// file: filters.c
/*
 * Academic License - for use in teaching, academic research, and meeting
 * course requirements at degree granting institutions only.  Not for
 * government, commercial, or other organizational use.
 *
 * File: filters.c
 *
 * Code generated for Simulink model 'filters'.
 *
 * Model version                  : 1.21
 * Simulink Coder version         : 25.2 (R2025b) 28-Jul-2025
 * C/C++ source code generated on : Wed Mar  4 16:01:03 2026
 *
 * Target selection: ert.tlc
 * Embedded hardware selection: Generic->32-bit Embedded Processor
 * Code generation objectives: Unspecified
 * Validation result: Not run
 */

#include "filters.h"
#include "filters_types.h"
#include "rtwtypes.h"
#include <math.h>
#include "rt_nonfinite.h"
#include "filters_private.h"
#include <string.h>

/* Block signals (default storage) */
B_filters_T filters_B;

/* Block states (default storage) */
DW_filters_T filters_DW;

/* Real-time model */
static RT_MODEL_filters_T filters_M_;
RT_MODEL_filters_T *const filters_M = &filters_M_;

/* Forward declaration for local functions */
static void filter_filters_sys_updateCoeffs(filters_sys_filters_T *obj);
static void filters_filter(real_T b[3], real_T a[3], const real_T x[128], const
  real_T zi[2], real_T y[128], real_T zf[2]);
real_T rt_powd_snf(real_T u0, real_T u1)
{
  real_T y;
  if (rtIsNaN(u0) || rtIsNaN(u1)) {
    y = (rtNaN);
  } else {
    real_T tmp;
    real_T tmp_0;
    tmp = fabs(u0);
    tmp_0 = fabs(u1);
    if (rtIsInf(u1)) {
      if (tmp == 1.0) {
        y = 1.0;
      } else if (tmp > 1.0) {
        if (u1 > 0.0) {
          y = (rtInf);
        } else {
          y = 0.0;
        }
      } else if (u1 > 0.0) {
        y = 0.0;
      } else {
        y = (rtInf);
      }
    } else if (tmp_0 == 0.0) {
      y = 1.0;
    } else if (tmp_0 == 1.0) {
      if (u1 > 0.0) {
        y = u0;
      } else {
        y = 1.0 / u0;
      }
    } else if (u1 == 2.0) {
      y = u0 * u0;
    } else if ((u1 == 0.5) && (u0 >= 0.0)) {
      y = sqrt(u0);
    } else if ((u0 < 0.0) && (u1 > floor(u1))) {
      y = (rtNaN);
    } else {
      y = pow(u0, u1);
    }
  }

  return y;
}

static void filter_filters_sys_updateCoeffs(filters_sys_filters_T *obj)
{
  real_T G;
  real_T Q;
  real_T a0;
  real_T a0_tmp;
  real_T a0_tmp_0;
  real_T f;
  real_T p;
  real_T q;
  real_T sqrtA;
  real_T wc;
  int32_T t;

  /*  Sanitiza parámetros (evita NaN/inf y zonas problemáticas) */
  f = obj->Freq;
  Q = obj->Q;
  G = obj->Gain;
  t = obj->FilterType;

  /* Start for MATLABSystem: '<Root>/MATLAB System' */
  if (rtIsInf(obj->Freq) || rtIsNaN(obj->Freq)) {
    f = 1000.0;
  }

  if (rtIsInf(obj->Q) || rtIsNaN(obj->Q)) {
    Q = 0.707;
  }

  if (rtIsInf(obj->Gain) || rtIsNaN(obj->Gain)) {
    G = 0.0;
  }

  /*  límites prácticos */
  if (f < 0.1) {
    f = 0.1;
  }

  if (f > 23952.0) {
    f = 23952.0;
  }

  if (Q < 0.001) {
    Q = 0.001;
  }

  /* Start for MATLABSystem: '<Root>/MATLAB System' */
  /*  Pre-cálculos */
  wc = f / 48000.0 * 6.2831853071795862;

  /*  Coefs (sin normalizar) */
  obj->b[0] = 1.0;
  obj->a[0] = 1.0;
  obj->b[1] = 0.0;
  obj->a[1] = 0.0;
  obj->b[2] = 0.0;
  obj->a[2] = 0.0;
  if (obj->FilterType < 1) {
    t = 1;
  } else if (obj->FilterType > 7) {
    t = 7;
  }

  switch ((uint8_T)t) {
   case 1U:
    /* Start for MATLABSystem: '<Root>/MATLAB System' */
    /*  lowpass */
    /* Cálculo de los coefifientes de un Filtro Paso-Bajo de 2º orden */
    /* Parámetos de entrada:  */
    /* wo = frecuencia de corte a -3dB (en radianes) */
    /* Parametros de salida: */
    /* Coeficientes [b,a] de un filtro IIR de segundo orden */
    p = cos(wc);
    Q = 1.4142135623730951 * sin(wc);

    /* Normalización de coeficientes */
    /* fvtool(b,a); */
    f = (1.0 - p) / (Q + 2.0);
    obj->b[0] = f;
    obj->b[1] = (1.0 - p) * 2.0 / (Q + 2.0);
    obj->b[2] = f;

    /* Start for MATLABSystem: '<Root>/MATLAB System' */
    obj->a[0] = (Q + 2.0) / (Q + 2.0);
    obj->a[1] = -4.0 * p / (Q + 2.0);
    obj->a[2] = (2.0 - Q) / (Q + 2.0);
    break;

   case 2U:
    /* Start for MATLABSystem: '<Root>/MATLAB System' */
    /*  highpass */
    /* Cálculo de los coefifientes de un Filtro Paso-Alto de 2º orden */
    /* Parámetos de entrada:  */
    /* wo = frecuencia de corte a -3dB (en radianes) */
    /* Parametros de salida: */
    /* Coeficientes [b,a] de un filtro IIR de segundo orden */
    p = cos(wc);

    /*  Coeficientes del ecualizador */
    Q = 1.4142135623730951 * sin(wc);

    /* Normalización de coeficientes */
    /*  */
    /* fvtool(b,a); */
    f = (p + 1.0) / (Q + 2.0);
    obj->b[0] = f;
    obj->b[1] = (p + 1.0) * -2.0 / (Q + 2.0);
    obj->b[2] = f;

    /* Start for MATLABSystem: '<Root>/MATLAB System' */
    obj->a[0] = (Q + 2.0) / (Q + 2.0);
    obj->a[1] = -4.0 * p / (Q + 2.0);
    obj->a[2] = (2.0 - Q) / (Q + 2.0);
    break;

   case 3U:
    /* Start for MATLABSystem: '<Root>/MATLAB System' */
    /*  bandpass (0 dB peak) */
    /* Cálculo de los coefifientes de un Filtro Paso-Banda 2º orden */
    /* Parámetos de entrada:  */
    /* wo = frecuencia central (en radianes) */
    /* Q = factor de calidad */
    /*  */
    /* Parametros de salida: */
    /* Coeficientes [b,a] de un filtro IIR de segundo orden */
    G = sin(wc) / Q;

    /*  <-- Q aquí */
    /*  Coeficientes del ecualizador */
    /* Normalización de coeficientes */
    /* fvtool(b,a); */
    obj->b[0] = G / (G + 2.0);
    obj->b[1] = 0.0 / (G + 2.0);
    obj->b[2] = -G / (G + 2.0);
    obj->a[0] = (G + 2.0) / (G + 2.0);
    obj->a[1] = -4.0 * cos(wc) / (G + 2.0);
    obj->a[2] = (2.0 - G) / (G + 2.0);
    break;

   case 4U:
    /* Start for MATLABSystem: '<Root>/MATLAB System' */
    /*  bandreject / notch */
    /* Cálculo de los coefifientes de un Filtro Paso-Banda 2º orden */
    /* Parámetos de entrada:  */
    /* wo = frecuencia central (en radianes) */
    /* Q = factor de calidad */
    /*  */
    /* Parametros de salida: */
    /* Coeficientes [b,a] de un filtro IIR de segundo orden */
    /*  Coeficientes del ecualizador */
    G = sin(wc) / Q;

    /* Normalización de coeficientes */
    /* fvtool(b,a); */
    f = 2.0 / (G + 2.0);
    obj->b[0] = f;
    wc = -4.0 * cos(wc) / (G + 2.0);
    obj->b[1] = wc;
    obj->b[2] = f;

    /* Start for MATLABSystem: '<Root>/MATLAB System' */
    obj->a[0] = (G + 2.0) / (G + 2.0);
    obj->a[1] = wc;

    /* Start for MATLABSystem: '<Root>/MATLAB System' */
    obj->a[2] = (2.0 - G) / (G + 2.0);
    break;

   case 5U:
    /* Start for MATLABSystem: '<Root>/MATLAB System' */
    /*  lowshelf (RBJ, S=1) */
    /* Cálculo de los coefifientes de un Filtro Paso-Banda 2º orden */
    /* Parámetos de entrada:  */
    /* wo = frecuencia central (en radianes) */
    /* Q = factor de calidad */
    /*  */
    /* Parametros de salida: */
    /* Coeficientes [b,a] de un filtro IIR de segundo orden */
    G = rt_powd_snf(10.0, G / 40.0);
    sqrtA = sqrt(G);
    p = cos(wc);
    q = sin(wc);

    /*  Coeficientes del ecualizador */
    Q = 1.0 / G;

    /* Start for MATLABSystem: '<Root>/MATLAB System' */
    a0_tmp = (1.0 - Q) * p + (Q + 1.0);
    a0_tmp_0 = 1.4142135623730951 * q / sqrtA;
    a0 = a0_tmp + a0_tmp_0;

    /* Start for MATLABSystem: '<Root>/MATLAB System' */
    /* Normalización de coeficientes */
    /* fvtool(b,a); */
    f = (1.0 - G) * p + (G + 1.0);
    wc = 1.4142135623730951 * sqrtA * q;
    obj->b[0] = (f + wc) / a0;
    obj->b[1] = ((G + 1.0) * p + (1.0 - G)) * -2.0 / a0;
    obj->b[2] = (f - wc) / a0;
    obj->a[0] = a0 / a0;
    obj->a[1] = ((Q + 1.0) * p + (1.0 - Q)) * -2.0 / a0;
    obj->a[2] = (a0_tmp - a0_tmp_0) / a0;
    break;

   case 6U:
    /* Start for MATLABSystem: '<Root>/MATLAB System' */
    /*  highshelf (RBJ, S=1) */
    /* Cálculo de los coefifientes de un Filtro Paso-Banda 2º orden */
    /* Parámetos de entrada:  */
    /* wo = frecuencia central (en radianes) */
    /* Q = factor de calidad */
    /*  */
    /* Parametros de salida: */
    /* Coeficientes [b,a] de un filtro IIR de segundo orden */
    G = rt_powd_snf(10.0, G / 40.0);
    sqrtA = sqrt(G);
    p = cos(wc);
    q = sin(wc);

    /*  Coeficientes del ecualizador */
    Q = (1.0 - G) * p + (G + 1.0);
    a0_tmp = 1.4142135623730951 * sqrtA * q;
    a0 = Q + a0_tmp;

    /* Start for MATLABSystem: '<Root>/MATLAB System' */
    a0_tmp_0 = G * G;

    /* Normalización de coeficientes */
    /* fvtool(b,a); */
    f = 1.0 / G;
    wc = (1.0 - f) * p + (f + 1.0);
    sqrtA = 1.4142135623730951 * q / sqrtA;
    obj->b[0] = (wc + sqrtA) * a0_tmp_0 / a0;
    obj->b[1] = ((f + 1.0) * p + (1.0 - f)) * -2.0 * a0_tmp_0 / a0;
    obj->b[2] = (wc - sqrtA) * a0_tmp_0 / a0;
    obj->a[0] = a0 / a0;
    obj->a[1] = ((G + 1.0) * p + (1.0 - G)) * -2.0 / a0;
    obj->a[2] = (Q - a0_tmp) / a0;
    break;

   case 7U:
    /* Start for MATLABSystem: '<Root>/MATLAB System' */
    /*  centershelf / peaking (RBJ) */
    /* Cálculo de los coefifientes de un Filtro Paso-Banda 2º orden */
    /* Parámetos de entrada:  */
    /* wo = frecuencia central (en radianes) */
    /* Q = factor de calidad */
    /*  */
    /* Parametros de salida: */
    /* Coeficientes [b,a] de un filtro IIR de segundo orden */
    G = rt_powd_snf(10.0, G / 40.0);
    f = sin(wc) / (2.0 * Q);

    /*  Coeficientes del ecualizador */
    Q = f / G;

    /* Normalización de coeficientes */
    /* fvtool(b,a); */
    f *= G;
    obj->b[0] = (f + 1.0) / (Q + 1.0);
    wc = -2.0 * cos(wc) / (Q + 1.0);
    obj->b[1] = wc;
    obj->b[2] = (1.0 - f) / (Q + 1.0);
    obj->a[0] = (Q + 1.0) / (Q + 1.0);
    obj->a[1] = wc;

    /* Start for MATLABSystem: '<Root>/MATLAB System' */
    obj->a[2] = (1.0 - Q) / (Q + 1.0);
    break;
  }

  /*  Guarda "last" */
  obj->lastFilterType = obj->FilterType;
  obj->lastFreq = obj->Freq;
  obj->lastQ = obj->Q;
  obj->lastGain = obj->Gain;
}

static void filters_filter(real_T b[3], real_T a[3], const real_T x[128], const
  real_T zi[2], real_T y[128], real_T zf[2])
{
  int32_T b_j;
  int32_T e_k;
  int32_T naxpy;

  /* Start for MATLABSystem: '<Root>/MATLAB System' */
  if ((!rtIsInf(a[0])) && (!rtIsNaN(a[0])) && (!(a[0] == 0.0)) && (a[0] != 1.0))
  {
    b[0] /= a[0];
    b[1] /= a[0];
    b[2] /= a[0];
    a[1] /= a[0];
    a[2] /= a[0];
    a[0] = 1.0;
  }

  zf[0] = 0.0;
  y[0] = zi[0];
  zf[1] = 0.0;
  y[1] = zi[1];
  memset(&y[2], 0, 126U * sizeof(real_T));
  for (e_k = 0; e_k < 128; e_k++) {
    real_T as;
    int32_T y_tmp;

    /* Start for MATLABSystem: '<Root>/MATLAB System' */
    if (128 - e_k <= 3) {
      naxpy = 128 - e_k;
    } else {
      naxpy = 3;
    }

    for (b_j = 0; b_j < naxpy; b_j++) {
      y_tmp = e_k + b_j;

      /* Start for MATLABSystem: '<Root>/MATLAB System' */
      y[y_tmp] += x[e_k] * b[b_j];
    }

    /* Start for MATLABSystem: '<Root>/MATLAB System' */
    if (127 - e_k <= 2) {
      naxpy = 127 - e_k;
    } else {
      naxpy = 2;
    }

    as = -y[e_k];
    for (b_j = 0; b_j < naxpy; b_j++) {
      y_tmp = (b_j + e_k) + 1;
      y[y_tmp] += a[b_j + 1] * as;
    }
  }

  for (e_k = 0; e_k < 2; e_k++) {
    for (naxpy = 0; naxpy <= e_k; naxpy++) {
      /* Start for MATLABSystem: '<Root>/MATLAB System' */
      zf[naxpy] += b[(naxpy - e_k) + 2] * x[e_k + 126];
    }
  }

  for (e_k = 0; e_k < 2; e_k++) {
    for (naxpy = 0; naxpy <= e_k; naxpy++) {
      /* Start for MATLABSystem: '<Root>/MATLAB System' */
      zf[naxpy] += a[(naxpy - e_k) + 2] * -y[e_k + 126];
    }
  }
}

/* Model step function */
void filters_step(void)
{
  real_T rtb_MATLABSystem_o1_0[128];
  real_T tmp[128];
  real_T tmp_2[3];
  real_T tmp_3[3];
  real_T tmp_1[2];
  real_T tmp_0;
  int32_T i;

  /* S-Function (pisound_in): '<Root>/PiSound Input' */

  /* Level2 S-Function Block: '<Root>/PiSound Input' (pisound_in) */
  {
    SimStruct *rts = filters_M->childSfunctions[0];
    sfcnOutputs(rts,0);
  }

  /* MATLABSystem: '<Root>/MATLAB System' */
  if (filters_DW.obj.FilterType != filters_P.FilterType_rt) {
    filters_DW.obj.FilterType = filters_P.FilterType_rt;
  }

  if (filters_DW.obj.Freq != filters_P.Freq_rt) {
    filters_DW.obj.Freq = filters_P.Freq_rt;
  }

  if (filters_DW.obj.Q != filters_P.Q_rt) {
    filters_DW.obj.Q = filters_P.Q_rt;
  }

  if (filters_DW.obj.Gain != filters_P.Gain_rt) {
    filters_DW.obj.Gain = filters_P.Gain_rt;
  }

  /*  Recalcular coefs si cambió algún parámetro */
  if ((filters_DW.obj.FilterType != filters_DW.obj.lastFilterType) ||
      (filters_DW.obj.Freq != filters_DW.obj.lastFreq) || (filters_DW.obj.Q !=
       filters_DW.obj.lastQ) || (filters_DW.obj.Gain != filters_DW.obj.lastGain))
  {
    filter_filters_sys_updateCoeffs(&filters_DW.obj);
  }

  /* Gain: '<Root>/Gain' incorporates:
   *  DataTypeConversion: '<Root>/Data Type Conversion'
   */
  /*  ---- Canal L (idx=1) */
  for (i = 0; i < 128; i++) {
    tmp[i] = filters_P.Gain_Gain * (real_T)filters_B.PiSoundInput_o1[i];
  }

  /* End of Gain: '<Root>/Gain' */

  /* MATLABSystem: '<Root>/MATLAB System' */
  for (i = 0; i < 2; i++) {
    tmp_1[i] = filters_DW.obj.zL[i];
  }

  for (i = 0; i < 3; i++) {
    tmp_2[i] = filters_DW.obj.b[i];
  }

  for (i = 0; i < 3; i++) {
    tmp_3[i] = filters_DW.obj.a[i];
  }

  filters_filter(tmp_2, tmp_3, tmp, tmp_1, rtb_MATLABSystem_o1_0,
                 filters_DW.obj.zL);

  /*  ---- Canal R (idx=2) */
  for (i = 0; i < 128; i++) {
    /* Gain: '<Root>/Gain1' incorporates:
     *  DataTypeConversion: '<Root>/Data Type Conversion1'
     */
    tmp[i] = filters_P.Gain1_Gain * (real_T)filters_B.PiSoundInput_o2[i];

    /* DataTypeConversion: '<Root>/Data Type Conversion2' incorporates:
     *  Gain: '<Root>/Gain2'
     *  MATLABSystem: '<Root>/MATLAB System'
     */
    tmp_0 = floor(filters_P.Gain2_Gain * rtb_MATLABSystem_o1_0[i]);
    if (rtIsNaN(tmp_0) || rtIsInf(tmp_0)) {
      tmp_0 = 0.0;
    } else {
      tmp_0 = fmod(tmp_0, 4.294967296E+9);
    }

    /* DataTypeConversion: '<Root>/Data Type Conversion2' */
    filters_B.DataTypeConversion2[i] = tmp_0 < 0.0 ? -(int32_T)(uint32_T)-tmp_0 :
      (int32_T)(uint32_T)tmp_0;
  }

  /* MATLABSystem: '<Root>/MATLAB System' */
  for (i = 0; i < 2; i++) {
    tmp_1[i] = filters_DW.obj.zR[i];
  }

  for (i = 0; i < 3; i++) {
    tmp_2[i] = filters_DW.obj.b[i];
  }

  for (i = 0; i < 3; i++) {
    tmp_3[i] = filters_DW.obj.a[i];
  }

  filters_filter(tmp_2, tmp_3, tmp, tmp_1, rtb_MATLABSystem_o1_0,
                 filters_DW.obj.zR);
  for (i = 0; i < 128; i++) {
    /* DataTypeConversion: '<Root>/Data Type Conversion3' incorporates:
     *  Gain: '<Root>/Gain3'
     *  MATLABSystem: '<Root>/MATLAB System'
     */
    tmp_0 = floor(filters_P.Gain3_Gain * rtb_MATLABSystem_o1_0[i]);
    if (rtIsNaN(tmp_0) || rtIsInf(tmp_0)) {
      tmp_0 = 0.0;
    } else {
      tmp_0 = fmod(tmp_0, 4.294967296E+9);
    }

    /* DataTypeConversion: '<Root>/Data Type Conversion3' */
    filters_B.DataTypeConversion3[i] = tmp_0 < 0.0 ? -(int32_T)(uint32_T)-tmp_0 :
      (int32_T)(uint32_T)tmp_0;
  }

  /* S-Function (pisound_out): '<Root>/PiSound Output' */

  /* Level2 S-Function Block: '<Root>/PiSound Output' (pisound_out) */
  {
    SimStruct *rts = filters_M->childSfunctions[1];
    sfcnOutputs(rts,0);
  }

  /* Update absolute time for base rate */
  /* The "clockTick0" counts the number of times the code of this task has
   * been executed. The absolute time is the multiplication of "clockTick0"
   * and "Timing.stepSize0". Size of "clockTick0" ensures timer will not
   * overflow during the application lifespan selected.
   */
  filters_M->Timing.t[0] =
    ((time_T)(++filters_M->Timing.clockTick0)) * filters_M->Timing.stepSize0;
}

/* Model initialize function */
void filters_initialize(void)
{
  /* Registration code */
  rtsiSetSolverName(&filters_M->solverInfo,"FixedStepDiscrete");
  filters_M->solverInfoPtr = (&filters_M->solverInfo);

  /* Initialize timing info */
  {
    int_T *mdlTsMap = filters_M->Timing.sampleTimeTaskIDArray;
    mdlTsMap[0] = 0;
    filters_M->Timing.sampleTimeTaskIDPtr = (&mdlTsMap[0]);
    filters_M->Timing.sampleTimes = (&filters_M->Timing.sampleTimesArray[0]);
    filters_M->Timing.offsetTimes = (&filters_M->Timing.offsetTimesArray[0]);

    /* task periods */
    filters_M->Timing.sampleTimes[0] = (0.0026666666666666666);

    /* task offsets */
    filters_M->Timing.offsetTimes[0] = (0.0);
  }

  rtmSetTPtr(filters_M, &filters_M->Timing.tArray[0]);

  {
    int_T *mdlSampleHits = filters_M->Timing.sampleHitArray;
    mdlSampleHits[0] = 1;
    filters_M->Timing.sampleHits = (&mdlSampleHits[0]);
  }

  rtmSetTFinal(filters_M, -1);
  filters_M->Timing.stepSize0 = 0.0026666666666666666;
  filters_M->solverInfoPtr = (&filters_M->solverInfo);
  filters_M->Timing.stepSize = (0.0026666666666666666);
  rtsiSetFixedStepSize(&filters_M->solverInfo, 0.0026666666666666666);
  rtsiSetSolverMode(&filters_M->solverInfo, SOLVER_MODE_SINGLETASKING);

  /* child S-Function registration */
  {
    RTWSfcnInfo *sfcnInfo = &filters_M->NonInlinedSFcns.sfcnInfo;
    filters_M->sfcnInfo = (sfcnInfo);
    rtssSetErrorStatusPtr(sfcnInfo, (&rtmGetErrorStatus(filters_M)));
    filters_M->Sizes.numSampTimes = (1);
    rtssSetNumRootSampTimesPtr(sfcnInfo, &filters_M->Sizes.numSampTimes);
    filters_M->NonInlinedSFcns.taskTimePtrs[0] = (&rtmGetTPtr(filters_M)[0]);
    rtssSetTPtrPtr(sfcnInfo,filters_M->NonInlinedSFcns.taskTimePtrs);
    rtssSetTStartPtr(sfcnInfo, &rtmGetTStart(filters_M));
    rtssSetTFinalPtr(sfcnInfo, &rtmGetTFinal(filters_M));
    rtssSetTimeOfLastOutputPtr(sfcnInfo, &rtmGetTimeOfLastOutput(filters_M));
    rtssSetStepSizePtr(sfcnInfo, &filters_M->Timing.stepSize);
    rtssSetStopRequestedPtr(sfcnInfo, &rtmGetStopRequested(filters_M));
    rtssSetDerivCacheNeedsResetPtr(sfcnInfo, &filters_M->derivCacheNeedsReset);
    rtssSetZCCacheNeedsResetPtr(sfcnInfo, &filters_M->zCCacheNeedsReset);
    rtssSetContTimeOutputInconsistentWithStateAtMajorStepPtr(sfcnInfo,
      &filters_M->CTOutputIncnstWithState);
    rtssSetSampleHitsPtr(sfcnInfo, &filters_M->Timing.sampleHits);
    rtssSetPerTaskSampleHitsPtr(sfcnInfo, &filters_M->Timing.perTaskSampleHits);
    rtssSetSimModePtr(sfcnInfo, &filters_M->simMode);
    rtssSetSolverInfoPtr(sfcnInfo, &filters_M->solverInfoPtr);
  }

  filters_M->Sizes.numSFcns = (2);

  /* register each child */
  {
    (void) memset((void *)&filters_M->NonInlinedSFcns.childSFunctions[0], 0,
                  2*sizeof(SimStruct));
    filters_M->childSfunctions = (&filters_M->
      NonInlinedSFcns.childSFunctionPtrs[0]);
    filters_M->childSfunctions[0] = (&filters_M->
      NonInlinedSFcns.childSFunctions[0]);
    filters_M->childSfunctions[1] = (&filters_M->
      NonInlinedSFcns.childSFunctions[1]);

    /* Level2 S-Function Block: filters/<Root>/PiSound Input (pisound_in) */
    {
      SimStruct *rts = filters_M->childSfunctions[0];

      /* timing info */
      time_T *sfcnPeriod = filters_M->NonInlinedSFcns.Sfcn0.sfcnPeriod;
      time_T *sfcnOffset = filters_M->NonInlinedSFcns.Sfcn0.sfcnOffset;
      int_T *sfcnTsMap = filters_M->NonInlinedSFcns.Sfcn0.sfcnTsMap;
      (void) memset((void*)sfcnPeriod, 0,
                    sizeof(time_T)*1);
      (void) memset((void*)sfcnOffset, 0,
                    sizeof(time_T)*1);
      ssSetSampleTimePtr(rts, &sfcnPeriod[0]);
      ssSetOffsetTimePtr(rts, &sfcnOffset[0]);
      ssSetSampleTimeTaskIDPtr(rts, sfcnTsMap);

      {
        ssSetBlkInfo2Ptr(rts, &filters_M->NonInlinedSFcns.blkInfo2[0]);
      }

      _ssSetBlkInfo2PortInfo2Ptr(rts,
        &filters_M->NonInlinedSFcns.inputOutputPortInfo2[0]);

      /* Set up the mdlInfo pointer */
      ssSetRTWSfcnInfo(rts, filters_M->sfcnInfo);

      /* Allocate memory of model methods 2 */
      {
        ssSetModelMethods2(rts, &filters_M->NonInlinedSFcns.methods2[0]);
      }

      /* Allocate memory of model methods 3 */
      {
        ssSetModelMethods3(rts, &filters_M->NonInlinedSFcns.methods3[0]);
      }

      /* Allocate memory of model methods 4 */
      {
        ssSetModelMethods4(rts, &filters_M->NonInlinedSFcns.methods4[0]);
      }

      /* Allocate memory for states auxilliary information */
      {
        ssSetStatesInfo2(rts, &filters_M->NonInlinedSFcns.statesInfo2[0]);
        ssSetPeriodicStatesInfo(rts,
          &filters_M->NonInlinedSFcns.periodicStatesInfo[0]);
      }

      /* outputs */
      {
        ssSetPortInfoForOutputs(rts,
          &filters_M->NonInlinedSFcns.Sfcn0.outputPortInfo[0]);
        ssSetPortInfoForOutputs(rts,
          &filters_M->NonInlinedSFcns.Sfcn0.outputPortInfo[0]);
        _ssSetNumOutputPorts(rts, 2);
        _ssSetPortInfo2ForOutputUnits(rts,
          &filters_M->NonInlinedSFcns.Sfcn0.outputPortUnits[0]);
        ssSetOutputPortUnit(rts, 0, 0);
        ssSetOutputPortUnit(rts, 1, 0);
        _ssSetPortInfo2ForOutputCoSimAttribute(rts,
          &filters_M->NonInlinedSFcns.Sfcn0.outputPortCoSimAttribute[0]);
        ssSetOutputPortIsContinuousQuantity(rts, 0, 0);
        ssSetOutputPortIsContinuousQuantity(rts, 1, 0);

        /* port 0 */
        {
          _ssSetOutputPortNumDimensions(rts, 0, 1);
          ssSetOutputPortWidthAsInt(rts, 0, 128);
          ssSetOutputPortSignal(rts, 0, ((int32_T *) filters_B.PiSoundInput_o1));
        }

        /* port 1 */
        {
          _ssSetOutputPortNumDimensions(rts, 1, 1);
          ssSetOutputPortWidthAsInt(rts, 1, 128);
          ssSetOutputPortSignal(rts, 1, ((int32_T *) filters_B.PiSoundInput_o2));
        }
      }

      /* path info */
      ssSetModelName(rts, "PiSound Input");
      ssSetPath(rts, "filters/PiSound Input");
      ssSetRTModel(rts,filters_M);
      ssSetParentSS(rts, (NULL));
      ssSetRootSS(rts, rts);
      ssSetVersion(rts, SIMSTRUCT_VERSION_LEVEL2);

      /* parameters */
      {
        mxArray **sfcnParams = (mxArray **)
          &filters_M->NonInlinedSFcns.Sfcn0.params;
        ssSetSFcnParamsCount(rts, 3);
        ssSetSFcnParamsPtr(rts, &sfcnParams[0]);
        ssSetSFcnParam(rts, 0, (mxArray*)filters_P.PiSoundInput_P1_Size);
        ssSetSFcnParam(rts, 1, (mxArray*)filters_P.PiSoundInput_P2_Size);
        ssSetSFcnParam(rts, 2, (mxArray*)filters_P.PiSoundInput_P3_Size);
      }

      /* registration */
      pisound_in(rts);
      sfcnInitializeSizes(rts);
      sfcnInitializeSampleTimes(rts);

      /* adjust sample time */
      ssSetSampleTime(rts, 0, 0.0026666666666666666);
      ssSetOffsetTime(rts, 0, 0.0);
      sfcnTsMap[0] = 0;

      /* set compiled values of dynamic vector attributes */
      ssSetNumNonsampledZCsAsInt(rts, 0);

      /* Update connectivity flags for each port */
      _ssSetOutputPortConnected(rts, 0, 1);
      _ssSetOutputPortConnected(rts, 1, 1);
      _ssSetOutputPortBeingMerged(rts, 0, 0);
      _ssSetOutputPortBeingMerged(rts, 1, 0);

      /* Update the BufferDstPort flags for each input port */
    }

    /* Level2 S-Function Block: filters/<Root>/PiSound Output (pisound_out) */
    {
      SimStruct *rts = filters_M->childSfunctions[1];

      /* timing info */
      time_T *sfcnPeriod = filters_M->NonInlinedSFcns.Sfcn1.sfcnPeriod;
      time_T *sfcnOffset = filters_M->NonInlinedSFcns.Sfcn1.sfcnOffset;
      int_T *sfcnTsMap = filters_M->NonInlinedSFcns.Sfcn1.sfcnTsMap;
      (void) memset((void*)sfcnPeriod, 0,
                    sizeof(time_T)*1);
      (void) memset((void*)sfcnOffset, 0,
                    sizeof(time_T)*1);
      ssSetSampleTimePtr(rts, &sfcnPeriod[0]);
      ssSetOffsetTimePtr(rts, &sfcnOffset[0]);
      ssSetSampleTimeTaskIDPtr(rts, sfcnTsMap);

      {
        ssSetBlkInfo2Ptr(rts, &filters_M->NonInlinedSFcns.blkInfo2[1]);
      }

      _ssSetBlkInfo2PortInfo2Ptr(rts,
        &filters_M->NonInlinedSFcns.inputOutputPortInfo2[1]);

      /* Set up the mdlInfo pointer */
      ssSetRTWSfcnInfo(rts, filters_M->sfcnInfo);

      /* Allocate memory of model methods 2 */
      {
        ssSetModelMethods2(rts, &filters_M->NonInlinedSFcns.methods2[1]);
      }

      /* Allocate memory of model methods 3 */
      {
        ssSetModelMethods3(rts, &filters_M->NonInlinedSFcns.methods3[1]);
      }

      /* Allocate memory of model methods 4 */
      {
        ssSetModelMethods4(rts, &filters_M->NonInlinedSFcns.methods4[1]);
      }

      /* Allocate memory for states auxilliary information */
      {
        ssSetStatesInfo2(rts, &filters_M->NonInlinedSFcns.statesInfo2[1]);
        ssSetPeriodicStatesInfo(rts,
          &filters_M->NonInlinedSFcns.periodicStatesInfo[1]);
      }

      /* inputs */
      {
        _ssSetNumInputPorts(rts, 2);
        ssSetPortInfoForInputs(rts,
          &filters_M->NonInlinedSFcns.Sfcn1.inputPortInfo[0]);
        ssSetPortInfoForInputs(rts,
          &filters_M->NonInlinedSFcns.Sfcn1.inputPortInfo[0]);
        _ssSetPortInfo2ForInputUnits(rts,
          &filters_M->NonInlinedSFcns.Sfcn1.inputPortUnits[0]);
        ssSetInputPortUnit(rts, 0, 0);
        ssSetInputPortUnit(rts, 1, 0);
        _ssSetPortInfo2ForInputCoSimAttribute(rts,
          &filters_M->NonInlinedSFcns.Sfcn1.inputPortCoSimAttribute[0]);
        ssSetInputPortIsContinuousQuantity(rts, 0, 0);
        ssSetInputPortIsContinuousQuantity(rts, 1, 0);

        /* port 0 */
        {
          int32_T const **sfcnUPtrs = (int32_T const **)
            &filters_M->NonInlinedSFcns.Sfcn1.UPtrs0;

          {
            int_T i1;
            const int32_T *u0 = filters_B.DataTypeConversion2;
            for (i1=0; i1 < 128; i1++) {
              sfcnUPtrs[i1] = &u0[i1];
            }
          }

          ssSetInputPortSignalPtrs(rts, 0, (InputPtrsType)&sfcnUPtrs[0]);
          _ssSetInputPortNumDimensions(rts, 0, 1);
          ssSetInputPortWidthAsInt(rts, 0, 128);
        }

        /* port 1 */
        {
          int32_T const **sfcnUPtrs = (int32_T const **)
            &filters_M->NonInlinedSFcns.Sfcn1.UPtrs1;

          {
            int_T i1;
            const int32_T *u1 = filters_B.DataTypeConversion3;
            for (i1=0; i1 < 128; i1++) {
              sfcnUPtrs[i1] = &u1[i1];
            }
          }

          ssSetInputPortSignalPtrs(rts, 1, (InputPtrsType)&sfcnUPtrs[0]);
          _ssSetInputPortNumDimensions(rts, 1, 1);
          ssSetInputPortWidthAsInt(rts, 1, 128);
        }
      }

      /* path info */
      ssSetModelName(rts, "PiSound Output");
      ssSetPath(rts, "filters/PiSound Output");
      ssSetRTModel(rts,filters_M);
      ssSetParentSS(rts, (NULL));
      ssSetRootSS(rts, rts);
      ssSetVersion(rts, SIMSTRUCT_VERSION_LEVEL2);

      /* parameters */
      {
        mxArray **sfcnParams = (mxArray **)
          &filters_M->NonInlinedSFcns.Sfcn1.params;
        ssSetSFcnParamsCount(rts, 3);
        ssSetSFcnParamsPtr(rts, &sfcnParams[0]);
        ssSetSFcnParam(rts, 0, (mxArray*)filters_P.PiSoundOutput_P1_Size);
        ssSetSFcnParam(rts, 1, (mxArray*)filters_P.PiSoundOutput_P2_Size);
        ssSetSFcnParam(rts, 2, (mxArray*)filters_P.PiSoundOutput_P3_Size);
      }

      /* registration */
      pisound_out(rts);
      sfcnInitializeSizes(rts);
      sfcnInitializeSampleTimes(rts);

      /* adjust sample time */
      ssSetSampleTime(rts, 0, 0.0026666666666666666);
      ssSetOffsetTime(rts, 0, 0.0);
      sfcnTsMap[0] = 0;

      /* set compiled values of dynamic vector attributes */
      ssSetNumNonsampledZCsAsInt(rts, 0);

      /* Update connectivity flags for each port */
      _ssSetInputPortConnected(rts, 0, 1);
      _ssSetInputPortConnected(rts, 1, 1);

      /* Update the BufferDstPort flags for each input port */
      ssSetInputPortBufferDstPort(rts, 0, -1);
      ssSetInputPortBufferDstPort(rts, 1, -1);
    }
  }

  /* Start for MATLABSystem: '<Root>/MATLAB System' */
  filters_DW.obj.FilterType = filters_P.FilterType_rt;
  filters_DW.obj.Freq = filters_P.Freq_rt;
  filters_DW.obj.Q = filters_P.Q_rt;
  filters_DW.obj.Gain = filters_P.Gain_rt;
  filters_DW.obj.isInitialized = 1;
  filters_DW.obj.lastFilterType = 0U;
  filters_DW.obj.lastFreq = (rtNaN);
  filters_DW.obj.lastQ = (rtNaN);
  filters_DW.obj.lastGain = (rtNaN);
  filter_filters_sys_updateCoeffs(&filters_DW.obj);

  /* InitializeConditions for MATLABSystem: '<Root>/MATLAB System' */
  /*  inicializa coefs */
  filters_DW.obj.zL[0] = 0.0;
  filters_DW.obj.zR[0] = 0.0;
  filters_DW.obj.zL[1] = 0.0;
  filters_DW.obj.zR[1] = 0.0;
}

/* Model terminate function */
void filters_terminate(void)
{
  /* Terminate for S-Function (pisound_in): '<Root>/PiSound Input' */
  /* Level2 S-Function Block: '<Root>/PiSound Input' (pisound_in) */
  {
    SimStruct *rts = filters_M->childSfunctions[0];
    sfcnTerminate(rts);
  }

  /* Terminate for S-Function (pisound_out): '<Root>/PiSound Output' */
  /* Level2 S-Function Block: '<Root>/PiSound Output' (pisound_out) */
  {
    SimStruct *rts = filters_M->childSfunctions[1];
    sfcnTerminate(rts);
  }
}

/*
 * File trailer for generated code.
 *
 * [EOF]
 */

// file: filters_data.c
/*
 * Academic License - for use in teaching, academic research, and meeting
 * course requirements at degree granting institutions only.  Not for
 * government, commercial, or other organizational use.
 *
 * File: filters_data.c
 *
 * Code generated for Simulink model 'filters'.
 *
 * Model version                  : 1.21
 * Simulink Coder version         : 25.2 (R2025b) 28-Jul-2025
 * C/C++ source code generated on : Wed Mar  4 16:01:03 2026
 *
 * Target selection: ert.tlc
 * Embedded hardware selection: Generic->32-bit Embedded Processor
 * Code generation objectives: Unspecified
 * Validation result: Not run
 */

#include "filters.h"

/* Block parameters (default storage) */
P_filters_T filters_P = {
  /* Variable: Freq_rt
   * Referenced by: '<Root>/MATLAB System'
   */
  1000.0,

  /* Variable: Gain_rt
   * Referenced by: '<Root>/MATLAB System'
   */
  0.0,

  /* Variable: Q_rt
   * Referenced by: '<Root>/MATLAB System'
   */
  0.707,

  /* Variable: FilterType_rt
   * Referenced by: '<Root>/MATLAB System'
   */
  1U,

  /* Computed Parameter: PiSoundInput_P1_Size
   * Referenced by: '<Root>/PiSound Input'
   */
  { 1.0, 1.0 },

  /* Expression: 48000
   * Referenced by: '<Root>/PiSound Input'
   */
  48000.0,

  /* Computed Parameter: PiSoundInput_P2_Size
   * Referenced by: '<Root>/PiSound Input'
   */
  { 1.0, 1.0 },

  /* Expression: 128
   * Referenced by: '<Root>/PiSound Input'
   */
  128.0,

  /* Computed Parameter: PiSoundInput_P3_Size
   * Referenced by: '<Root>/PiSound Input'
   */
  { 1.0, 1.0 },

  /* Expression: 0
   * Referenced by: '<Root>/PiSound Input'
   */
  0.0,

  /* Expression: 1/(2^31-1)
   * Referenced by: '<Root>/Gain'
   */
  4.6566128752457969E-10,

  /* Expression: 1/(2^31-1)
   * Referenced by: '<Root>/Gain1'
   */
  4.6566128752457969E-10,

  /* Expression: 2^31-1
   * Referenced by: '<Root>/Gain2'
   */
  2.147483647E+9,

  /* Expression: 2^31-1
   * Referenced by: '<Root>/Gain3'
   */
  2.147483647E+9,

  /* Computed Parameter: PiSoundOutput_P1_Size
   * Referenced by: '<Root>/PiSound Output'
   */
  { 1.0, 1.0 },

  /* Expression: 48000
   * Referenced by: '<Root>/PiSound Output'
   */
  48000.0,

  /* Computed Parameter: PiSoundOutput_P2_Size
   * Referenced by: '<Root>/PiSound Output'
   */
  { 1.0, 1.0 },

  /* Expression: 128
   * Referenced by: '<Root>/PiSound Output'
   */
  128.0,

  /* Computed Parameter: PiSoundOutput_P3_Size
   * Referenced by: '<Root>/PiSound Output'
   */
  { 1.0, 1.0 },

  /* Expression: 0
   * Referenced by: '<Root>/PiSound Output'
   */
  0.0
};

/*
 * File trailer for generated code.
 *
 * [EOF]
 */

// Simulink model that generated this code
simulink model "filters"  (R2025b)
settings: Solver=FixedStepDiscrete  StartTime=0.0  StopTime=inf  RelTol=1e-3
undefined symbols (not defined in the file or in its folder): Gain_rt

== system filters ==
  Data Type Conversion : DataTypeConversion  OutDataTypeStr=double  SaturateOnIntegerOverflow=off  RndMeth=Floor
  Data Type Conversion1 : DataTypeConversion  OutDataTypeStr=double  SaturateOnIntegerOverflow=off  RndMeth=Floor
  Data Type Conversion2 : DataTypeConversion  OutDataTypeStr=int32  SaturateOnIntegerOverflow=off  RndMeth=Floor
  Data Type Conversion3 : DataTypeConversion  OutDataTypeStr=int32  SaturateOnIntegerOverflow=off  RndMeth=Floor
  Gain : Gain  Gain=1/(2^31-1)  Multiplication=Matrix(K*u)
  Gain1 : Gain  Gain=1/(2^31-1)  Multiplication=Matrix(K*u)
  Gain2 : Gain  Gain=2^31-1  Multiplication=Matrix(K*u)
  Gain3 : Gain  Gain=2^31-1  Multiplication=Matrix(K*u)
  MATLAB System : MATLABSystem  InitFcn=|  System=filters_sys  N=128  Fs=48000  FilterType=FilterType_rt  Freq=Freq_rt  Q=Q_rt  Gain=Gain_rt  SimulateUsing=Code generation
      | Type_rt = uint8(1);   % 1..7
      | Freq_rt = 1000;       % Hz
      | Q_rt    = 0.707;
      | Gain_rt = 0;          % dB
  PiSound Input : S-Function  FunctionName=pisound_in  Parameters=48000, 128, 0  SFunctionDeploymentMode=off  EnableBusSupport=off
  PiSound Output : S-Function  FunctionName=pisound_out  Parameters=48000, 128, 0  SFunctionDeploymentMode=off  EnableBusSupport=off
  wires:
  PiSound Input/1 -> Data Type Conversion/1
  PiSound Input/2 -> Data Type Conversion1/1
  Data Type Conversion/1 -> Gain/1
  Data Type Conversion1/1 -> Gain1/1
  Gain2/1 -> Data Type Conversion2/1
  Gain3/1 -> Data Type Conversion3/1
  Gain/1 -> MATLAB System/1
  MATLAB System/1 -> Gain2/1
  Gain1/1 -> MATLAB System/2
  MATLAB System/2 -> Gain3/1
  Data Type Conversion2/1 -> PiSound Output/1
  Data Type Conversion3/1 -> PiSound Output/2
